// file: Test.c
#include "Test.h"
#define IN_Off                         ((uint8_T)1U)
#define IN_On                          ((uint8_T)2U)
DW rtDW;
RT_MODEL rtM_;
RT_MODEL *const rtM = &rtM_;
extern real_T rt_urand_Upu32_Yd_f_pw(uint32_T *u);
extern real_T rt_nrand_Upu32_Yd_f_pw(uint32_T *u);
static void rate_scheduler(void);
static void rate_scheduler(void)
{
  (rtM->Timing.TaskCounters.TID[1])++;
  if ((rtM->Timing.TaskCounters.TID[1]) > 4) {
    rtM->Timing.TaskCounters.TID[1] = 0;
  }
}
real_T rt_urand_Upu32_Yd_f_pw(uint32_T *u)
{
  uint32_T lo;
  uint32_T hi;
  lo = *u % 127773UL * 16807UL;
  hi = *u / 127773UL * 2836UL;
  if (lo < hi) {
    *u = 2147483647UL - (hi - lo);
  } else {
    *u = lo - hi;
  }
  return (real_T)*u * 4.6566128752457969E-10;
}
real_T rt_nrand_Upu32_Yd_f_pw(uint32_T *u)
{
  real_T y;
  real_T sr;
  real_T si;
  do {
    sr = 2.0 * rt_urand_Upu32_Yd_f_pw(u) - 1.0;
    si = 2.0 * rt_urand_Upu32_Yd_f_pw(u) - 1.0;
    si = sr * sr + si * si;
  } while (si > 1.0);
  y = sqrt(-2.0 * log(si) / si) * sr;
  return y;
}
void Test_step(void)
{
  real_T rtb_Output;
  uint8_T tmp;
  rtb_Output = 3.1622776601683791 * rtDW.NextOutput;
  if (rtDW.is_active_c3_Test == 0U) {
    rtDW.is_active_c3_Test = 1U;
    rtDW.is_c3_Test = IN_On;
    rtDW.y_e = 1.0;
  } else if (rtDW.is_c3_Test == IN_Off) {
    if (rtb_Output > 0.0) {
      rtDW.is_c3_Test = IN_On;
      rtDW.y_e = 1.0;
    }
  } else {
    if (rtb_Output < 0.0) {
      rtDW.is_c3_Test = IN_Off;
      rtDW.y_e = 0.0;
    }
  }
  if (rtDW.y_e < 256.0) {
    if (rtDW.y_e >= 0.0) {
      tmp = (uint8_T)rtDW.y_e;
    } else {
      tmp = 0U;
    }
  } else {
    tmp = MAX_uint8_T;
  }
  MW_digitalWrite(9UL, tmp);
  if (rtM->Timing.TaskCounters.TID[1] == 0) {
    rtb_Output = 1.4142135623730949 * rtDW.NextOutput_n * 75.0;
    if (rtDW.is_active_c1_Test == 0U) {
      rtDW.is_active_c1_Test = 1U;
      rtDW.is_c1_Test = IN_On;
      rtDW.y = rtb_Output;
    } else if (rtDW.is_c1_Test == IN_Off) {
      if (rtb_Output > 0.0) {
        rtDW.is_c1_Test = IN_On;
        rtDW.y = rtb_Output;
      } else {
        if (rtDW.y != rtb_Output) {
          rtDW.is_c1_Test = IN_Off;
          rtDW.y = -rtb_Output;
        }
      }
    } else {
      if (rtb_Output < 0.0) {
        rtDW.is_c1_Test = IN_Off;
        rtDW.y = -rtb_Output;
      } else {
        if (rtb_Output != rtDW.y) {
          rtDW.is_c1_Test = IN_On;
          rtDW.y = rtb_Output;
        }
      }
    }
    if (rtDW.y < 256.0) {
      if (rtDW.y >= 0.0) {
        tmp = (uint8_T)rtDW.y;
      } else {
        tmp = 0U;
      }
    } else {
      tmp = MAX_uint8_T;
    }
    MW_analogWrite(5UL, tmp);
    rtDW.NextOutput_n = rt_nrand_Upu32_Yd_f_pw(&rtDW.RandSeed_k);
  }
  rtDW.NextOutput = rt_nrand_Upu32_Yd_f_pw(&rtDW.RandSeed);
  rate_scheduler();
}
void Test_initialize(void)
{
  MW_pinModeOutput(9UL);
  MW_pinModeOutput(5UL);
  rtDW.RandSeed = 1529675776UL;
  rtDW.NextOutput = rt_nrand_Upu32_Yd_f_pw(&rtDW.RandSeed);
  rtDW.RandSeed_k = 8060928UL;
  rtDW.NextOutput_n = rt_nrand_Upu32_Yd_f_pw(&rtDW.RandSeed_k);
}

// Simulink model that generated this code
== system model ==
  DigitalOutput#1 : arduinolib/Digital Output  pinNumber=9  <- 1: Stateflowchart#1
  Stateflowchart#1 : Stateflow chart  <- 1: BandLimitedWhiteNoise#1
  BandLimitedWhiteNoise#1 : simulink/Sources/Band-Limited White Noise
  PWM#1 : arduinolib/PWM  pinNumber=5  <- 1: Stateflowchart#2
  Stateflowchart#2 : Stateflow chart  <- 1: Gain#1
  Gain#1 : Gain  Gain=75  <- 1: BandLimitedWhiteNoise#2
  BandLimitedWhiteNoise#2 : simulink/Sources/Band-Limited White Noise
== stateflow chart Stateflowchart#2 ==
  state Off
    entry: y= u*(-1)
  state On
    entry: y = u*1
  (default) -> On
  On -> Off [order 1] : [u<0]
  Off -> On [order 1] : [u>0]
  Off -> Off [order 2] : [y~=u]
  On -> On [order 2] : [u~=y]
  data: u input; y output

== stateflow chart Stateflowchart#1 ==
  state Off
    entry: y=0
  state On
    entry: y = 1
  (default) -> On
  On -> Off : [u<0]
  Off -> On : [u>0]
  data: u input; y output
